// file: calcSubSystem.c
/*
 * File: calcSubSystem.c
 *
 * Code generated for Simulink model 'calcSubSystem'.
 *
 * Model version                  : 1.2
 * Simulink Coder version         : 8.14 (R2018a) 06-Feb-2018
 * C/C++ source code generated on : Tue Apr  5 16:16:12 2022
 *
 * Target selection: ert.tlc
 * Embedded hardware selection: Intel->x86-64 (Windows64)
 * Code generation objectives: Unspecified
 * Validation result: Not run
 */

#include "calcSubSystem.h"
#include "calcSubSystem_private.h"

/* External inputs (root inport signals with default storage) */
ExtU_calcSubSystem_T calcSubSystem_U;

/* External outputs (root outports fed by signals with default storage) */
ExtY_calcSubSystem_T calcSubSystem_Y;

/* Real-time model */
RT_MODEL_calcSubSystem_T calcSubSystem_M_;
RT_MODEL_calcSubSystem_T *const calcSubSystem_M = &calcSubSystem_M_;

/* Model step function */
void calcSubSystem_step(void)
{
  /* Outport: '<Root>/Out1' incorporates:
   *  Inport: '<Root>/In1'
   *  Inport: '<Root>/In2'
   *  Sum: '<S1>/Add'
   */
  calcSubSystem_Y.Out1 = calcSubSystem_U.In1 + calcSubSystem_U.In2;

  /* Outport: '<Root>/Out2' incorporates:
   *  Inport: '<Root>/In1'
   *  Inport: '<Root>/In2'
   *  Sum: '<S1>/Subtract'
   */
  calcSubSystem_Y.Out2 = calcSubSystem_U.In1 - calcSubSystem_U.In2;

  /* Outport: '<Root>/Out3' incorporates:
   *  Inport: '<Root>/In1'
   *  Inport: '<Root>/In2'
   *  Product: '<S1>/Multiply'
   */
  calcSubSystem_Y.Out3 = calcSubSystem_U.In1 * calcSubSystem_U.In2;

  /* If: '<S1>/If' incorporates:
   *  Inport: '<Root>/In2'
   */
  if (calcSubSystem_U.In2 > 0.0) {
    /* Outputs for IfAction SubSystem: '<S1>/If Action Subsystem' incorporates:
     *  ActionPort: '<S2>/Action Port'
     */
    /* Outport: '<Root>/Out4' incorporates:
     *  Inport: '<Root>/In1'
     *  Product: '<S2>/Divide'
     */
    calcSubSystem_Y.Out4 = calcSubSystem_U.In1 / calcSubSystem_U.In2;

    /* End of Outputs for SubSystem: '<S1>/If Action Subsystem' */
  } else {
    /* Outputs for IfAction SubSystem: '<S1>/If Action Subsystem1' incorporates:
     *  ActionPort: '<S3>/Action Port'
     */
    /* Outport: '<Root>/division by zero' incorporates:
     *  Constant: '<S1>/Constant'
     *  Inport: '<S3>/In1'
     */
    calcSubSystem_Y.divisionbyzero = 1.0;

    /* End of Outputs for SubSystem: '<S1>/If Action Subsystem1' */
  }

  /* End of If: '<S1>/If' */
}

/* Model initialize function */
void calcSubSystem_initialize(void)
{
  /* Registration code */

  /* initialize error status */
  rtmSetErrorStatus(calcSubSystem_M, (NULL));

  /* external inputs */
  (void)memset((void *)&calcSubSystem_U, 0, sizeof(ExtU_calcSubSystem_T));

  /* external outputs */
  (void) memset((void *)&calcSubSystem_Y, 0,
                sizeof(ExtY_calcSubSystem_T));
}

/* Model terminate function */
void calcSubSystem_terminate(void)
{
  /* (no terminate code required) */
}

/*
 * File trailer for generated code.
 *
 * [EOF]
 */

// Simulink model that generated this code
simulink model "calcSubSystem"  (R2018a)
settings: Solver=FixedStepDiscrete  StartTime=0.0  StopTime=10.0  RelTol=1e-3

== system calcSubSystem ==
  In1 : Inport
  In2 : Inport  Port=2
  Subsystem : Subsystem
  Out1 : Outport
  Out2 : Outport  Port=2
  Out3 : Outport  Port=3
  Out4 : Outport  Port=4
  division by zero : Outport  Port=5
  wires:
  In1/1 -> Subsystem/1(In1)
  In2/1 -> Subsystem/2(In2)
  Subsystem/1(Out1) -> Out1/1
  Subsystem/2(Out2) -> Out2/1
  Subsystem/3(Out3) -> Out3/1
  Subsystem/4(Out4) -> Out4/1
  Subsystem/5(division by zero) -> division by zero/1

== system calcSubSystem/Subsystem ==
  In1 : Inport
  In2 : Inport  Port=2
  Add : Sum
  Constant : Constant
  If : If  IfExpression="u1 >  0"
  If Action Subsystem : Subsystem  TreatAsAtomicUnit=on
  If Action Subsystem1 : Subsystem  TreatAsAtomicUnit=on
  Multiply : Product
  Subtract : Sum  Inputs=+-
  Out1 : Outport
  Out2 : Outport  Port=2
  Out3 : Outport  Port=3
  Out4 : Outport  Port=4
  division by zero : Outport  Port=5
  wires:
  In1/1 -> Multiply/1, Subtract/1, Add/1, If Action Subsystem/1(In1)
  If/1 -> If Action Subsystem/Action
  Constant/1 -> If Action Subsystem1/1(In1)
  In2/1 -> If/1, If Action Subsystem/2(In2), Multiply/2, Subtract/2, Add/2
  If/2 -> If Action Subsystem1/Action
  Subtract/1 -> Out2/1
  Multiply/1 -> Out3/1
  Add/1 -> Out1/1
  If Action Subsystem/1(Out1) -> Out4/1
  If Action Subsystem1/1(Out1) -> division by zero/1

== system calcSubSystem/Subsystem/If Action Subsystem ==
  In1 : Inport
  In2 : Inport  Port=2
  Action Port : ActionPort  ActionType=then
  Divide : Product  Inputs=*/
  Out1 : Outport
  wires:
  In1/1 -> Divide/1
  In2/1 -> Divide/2
  Divide/1 -> Out1/1

== system calcSubSystem/Subsystem/If Action Subsystem1 ==
  In1 : Inport
  Action Port : ActionPort  ActionType=else
  Out1 : Outport
  wires:
  In1/1 -> Out1/1
